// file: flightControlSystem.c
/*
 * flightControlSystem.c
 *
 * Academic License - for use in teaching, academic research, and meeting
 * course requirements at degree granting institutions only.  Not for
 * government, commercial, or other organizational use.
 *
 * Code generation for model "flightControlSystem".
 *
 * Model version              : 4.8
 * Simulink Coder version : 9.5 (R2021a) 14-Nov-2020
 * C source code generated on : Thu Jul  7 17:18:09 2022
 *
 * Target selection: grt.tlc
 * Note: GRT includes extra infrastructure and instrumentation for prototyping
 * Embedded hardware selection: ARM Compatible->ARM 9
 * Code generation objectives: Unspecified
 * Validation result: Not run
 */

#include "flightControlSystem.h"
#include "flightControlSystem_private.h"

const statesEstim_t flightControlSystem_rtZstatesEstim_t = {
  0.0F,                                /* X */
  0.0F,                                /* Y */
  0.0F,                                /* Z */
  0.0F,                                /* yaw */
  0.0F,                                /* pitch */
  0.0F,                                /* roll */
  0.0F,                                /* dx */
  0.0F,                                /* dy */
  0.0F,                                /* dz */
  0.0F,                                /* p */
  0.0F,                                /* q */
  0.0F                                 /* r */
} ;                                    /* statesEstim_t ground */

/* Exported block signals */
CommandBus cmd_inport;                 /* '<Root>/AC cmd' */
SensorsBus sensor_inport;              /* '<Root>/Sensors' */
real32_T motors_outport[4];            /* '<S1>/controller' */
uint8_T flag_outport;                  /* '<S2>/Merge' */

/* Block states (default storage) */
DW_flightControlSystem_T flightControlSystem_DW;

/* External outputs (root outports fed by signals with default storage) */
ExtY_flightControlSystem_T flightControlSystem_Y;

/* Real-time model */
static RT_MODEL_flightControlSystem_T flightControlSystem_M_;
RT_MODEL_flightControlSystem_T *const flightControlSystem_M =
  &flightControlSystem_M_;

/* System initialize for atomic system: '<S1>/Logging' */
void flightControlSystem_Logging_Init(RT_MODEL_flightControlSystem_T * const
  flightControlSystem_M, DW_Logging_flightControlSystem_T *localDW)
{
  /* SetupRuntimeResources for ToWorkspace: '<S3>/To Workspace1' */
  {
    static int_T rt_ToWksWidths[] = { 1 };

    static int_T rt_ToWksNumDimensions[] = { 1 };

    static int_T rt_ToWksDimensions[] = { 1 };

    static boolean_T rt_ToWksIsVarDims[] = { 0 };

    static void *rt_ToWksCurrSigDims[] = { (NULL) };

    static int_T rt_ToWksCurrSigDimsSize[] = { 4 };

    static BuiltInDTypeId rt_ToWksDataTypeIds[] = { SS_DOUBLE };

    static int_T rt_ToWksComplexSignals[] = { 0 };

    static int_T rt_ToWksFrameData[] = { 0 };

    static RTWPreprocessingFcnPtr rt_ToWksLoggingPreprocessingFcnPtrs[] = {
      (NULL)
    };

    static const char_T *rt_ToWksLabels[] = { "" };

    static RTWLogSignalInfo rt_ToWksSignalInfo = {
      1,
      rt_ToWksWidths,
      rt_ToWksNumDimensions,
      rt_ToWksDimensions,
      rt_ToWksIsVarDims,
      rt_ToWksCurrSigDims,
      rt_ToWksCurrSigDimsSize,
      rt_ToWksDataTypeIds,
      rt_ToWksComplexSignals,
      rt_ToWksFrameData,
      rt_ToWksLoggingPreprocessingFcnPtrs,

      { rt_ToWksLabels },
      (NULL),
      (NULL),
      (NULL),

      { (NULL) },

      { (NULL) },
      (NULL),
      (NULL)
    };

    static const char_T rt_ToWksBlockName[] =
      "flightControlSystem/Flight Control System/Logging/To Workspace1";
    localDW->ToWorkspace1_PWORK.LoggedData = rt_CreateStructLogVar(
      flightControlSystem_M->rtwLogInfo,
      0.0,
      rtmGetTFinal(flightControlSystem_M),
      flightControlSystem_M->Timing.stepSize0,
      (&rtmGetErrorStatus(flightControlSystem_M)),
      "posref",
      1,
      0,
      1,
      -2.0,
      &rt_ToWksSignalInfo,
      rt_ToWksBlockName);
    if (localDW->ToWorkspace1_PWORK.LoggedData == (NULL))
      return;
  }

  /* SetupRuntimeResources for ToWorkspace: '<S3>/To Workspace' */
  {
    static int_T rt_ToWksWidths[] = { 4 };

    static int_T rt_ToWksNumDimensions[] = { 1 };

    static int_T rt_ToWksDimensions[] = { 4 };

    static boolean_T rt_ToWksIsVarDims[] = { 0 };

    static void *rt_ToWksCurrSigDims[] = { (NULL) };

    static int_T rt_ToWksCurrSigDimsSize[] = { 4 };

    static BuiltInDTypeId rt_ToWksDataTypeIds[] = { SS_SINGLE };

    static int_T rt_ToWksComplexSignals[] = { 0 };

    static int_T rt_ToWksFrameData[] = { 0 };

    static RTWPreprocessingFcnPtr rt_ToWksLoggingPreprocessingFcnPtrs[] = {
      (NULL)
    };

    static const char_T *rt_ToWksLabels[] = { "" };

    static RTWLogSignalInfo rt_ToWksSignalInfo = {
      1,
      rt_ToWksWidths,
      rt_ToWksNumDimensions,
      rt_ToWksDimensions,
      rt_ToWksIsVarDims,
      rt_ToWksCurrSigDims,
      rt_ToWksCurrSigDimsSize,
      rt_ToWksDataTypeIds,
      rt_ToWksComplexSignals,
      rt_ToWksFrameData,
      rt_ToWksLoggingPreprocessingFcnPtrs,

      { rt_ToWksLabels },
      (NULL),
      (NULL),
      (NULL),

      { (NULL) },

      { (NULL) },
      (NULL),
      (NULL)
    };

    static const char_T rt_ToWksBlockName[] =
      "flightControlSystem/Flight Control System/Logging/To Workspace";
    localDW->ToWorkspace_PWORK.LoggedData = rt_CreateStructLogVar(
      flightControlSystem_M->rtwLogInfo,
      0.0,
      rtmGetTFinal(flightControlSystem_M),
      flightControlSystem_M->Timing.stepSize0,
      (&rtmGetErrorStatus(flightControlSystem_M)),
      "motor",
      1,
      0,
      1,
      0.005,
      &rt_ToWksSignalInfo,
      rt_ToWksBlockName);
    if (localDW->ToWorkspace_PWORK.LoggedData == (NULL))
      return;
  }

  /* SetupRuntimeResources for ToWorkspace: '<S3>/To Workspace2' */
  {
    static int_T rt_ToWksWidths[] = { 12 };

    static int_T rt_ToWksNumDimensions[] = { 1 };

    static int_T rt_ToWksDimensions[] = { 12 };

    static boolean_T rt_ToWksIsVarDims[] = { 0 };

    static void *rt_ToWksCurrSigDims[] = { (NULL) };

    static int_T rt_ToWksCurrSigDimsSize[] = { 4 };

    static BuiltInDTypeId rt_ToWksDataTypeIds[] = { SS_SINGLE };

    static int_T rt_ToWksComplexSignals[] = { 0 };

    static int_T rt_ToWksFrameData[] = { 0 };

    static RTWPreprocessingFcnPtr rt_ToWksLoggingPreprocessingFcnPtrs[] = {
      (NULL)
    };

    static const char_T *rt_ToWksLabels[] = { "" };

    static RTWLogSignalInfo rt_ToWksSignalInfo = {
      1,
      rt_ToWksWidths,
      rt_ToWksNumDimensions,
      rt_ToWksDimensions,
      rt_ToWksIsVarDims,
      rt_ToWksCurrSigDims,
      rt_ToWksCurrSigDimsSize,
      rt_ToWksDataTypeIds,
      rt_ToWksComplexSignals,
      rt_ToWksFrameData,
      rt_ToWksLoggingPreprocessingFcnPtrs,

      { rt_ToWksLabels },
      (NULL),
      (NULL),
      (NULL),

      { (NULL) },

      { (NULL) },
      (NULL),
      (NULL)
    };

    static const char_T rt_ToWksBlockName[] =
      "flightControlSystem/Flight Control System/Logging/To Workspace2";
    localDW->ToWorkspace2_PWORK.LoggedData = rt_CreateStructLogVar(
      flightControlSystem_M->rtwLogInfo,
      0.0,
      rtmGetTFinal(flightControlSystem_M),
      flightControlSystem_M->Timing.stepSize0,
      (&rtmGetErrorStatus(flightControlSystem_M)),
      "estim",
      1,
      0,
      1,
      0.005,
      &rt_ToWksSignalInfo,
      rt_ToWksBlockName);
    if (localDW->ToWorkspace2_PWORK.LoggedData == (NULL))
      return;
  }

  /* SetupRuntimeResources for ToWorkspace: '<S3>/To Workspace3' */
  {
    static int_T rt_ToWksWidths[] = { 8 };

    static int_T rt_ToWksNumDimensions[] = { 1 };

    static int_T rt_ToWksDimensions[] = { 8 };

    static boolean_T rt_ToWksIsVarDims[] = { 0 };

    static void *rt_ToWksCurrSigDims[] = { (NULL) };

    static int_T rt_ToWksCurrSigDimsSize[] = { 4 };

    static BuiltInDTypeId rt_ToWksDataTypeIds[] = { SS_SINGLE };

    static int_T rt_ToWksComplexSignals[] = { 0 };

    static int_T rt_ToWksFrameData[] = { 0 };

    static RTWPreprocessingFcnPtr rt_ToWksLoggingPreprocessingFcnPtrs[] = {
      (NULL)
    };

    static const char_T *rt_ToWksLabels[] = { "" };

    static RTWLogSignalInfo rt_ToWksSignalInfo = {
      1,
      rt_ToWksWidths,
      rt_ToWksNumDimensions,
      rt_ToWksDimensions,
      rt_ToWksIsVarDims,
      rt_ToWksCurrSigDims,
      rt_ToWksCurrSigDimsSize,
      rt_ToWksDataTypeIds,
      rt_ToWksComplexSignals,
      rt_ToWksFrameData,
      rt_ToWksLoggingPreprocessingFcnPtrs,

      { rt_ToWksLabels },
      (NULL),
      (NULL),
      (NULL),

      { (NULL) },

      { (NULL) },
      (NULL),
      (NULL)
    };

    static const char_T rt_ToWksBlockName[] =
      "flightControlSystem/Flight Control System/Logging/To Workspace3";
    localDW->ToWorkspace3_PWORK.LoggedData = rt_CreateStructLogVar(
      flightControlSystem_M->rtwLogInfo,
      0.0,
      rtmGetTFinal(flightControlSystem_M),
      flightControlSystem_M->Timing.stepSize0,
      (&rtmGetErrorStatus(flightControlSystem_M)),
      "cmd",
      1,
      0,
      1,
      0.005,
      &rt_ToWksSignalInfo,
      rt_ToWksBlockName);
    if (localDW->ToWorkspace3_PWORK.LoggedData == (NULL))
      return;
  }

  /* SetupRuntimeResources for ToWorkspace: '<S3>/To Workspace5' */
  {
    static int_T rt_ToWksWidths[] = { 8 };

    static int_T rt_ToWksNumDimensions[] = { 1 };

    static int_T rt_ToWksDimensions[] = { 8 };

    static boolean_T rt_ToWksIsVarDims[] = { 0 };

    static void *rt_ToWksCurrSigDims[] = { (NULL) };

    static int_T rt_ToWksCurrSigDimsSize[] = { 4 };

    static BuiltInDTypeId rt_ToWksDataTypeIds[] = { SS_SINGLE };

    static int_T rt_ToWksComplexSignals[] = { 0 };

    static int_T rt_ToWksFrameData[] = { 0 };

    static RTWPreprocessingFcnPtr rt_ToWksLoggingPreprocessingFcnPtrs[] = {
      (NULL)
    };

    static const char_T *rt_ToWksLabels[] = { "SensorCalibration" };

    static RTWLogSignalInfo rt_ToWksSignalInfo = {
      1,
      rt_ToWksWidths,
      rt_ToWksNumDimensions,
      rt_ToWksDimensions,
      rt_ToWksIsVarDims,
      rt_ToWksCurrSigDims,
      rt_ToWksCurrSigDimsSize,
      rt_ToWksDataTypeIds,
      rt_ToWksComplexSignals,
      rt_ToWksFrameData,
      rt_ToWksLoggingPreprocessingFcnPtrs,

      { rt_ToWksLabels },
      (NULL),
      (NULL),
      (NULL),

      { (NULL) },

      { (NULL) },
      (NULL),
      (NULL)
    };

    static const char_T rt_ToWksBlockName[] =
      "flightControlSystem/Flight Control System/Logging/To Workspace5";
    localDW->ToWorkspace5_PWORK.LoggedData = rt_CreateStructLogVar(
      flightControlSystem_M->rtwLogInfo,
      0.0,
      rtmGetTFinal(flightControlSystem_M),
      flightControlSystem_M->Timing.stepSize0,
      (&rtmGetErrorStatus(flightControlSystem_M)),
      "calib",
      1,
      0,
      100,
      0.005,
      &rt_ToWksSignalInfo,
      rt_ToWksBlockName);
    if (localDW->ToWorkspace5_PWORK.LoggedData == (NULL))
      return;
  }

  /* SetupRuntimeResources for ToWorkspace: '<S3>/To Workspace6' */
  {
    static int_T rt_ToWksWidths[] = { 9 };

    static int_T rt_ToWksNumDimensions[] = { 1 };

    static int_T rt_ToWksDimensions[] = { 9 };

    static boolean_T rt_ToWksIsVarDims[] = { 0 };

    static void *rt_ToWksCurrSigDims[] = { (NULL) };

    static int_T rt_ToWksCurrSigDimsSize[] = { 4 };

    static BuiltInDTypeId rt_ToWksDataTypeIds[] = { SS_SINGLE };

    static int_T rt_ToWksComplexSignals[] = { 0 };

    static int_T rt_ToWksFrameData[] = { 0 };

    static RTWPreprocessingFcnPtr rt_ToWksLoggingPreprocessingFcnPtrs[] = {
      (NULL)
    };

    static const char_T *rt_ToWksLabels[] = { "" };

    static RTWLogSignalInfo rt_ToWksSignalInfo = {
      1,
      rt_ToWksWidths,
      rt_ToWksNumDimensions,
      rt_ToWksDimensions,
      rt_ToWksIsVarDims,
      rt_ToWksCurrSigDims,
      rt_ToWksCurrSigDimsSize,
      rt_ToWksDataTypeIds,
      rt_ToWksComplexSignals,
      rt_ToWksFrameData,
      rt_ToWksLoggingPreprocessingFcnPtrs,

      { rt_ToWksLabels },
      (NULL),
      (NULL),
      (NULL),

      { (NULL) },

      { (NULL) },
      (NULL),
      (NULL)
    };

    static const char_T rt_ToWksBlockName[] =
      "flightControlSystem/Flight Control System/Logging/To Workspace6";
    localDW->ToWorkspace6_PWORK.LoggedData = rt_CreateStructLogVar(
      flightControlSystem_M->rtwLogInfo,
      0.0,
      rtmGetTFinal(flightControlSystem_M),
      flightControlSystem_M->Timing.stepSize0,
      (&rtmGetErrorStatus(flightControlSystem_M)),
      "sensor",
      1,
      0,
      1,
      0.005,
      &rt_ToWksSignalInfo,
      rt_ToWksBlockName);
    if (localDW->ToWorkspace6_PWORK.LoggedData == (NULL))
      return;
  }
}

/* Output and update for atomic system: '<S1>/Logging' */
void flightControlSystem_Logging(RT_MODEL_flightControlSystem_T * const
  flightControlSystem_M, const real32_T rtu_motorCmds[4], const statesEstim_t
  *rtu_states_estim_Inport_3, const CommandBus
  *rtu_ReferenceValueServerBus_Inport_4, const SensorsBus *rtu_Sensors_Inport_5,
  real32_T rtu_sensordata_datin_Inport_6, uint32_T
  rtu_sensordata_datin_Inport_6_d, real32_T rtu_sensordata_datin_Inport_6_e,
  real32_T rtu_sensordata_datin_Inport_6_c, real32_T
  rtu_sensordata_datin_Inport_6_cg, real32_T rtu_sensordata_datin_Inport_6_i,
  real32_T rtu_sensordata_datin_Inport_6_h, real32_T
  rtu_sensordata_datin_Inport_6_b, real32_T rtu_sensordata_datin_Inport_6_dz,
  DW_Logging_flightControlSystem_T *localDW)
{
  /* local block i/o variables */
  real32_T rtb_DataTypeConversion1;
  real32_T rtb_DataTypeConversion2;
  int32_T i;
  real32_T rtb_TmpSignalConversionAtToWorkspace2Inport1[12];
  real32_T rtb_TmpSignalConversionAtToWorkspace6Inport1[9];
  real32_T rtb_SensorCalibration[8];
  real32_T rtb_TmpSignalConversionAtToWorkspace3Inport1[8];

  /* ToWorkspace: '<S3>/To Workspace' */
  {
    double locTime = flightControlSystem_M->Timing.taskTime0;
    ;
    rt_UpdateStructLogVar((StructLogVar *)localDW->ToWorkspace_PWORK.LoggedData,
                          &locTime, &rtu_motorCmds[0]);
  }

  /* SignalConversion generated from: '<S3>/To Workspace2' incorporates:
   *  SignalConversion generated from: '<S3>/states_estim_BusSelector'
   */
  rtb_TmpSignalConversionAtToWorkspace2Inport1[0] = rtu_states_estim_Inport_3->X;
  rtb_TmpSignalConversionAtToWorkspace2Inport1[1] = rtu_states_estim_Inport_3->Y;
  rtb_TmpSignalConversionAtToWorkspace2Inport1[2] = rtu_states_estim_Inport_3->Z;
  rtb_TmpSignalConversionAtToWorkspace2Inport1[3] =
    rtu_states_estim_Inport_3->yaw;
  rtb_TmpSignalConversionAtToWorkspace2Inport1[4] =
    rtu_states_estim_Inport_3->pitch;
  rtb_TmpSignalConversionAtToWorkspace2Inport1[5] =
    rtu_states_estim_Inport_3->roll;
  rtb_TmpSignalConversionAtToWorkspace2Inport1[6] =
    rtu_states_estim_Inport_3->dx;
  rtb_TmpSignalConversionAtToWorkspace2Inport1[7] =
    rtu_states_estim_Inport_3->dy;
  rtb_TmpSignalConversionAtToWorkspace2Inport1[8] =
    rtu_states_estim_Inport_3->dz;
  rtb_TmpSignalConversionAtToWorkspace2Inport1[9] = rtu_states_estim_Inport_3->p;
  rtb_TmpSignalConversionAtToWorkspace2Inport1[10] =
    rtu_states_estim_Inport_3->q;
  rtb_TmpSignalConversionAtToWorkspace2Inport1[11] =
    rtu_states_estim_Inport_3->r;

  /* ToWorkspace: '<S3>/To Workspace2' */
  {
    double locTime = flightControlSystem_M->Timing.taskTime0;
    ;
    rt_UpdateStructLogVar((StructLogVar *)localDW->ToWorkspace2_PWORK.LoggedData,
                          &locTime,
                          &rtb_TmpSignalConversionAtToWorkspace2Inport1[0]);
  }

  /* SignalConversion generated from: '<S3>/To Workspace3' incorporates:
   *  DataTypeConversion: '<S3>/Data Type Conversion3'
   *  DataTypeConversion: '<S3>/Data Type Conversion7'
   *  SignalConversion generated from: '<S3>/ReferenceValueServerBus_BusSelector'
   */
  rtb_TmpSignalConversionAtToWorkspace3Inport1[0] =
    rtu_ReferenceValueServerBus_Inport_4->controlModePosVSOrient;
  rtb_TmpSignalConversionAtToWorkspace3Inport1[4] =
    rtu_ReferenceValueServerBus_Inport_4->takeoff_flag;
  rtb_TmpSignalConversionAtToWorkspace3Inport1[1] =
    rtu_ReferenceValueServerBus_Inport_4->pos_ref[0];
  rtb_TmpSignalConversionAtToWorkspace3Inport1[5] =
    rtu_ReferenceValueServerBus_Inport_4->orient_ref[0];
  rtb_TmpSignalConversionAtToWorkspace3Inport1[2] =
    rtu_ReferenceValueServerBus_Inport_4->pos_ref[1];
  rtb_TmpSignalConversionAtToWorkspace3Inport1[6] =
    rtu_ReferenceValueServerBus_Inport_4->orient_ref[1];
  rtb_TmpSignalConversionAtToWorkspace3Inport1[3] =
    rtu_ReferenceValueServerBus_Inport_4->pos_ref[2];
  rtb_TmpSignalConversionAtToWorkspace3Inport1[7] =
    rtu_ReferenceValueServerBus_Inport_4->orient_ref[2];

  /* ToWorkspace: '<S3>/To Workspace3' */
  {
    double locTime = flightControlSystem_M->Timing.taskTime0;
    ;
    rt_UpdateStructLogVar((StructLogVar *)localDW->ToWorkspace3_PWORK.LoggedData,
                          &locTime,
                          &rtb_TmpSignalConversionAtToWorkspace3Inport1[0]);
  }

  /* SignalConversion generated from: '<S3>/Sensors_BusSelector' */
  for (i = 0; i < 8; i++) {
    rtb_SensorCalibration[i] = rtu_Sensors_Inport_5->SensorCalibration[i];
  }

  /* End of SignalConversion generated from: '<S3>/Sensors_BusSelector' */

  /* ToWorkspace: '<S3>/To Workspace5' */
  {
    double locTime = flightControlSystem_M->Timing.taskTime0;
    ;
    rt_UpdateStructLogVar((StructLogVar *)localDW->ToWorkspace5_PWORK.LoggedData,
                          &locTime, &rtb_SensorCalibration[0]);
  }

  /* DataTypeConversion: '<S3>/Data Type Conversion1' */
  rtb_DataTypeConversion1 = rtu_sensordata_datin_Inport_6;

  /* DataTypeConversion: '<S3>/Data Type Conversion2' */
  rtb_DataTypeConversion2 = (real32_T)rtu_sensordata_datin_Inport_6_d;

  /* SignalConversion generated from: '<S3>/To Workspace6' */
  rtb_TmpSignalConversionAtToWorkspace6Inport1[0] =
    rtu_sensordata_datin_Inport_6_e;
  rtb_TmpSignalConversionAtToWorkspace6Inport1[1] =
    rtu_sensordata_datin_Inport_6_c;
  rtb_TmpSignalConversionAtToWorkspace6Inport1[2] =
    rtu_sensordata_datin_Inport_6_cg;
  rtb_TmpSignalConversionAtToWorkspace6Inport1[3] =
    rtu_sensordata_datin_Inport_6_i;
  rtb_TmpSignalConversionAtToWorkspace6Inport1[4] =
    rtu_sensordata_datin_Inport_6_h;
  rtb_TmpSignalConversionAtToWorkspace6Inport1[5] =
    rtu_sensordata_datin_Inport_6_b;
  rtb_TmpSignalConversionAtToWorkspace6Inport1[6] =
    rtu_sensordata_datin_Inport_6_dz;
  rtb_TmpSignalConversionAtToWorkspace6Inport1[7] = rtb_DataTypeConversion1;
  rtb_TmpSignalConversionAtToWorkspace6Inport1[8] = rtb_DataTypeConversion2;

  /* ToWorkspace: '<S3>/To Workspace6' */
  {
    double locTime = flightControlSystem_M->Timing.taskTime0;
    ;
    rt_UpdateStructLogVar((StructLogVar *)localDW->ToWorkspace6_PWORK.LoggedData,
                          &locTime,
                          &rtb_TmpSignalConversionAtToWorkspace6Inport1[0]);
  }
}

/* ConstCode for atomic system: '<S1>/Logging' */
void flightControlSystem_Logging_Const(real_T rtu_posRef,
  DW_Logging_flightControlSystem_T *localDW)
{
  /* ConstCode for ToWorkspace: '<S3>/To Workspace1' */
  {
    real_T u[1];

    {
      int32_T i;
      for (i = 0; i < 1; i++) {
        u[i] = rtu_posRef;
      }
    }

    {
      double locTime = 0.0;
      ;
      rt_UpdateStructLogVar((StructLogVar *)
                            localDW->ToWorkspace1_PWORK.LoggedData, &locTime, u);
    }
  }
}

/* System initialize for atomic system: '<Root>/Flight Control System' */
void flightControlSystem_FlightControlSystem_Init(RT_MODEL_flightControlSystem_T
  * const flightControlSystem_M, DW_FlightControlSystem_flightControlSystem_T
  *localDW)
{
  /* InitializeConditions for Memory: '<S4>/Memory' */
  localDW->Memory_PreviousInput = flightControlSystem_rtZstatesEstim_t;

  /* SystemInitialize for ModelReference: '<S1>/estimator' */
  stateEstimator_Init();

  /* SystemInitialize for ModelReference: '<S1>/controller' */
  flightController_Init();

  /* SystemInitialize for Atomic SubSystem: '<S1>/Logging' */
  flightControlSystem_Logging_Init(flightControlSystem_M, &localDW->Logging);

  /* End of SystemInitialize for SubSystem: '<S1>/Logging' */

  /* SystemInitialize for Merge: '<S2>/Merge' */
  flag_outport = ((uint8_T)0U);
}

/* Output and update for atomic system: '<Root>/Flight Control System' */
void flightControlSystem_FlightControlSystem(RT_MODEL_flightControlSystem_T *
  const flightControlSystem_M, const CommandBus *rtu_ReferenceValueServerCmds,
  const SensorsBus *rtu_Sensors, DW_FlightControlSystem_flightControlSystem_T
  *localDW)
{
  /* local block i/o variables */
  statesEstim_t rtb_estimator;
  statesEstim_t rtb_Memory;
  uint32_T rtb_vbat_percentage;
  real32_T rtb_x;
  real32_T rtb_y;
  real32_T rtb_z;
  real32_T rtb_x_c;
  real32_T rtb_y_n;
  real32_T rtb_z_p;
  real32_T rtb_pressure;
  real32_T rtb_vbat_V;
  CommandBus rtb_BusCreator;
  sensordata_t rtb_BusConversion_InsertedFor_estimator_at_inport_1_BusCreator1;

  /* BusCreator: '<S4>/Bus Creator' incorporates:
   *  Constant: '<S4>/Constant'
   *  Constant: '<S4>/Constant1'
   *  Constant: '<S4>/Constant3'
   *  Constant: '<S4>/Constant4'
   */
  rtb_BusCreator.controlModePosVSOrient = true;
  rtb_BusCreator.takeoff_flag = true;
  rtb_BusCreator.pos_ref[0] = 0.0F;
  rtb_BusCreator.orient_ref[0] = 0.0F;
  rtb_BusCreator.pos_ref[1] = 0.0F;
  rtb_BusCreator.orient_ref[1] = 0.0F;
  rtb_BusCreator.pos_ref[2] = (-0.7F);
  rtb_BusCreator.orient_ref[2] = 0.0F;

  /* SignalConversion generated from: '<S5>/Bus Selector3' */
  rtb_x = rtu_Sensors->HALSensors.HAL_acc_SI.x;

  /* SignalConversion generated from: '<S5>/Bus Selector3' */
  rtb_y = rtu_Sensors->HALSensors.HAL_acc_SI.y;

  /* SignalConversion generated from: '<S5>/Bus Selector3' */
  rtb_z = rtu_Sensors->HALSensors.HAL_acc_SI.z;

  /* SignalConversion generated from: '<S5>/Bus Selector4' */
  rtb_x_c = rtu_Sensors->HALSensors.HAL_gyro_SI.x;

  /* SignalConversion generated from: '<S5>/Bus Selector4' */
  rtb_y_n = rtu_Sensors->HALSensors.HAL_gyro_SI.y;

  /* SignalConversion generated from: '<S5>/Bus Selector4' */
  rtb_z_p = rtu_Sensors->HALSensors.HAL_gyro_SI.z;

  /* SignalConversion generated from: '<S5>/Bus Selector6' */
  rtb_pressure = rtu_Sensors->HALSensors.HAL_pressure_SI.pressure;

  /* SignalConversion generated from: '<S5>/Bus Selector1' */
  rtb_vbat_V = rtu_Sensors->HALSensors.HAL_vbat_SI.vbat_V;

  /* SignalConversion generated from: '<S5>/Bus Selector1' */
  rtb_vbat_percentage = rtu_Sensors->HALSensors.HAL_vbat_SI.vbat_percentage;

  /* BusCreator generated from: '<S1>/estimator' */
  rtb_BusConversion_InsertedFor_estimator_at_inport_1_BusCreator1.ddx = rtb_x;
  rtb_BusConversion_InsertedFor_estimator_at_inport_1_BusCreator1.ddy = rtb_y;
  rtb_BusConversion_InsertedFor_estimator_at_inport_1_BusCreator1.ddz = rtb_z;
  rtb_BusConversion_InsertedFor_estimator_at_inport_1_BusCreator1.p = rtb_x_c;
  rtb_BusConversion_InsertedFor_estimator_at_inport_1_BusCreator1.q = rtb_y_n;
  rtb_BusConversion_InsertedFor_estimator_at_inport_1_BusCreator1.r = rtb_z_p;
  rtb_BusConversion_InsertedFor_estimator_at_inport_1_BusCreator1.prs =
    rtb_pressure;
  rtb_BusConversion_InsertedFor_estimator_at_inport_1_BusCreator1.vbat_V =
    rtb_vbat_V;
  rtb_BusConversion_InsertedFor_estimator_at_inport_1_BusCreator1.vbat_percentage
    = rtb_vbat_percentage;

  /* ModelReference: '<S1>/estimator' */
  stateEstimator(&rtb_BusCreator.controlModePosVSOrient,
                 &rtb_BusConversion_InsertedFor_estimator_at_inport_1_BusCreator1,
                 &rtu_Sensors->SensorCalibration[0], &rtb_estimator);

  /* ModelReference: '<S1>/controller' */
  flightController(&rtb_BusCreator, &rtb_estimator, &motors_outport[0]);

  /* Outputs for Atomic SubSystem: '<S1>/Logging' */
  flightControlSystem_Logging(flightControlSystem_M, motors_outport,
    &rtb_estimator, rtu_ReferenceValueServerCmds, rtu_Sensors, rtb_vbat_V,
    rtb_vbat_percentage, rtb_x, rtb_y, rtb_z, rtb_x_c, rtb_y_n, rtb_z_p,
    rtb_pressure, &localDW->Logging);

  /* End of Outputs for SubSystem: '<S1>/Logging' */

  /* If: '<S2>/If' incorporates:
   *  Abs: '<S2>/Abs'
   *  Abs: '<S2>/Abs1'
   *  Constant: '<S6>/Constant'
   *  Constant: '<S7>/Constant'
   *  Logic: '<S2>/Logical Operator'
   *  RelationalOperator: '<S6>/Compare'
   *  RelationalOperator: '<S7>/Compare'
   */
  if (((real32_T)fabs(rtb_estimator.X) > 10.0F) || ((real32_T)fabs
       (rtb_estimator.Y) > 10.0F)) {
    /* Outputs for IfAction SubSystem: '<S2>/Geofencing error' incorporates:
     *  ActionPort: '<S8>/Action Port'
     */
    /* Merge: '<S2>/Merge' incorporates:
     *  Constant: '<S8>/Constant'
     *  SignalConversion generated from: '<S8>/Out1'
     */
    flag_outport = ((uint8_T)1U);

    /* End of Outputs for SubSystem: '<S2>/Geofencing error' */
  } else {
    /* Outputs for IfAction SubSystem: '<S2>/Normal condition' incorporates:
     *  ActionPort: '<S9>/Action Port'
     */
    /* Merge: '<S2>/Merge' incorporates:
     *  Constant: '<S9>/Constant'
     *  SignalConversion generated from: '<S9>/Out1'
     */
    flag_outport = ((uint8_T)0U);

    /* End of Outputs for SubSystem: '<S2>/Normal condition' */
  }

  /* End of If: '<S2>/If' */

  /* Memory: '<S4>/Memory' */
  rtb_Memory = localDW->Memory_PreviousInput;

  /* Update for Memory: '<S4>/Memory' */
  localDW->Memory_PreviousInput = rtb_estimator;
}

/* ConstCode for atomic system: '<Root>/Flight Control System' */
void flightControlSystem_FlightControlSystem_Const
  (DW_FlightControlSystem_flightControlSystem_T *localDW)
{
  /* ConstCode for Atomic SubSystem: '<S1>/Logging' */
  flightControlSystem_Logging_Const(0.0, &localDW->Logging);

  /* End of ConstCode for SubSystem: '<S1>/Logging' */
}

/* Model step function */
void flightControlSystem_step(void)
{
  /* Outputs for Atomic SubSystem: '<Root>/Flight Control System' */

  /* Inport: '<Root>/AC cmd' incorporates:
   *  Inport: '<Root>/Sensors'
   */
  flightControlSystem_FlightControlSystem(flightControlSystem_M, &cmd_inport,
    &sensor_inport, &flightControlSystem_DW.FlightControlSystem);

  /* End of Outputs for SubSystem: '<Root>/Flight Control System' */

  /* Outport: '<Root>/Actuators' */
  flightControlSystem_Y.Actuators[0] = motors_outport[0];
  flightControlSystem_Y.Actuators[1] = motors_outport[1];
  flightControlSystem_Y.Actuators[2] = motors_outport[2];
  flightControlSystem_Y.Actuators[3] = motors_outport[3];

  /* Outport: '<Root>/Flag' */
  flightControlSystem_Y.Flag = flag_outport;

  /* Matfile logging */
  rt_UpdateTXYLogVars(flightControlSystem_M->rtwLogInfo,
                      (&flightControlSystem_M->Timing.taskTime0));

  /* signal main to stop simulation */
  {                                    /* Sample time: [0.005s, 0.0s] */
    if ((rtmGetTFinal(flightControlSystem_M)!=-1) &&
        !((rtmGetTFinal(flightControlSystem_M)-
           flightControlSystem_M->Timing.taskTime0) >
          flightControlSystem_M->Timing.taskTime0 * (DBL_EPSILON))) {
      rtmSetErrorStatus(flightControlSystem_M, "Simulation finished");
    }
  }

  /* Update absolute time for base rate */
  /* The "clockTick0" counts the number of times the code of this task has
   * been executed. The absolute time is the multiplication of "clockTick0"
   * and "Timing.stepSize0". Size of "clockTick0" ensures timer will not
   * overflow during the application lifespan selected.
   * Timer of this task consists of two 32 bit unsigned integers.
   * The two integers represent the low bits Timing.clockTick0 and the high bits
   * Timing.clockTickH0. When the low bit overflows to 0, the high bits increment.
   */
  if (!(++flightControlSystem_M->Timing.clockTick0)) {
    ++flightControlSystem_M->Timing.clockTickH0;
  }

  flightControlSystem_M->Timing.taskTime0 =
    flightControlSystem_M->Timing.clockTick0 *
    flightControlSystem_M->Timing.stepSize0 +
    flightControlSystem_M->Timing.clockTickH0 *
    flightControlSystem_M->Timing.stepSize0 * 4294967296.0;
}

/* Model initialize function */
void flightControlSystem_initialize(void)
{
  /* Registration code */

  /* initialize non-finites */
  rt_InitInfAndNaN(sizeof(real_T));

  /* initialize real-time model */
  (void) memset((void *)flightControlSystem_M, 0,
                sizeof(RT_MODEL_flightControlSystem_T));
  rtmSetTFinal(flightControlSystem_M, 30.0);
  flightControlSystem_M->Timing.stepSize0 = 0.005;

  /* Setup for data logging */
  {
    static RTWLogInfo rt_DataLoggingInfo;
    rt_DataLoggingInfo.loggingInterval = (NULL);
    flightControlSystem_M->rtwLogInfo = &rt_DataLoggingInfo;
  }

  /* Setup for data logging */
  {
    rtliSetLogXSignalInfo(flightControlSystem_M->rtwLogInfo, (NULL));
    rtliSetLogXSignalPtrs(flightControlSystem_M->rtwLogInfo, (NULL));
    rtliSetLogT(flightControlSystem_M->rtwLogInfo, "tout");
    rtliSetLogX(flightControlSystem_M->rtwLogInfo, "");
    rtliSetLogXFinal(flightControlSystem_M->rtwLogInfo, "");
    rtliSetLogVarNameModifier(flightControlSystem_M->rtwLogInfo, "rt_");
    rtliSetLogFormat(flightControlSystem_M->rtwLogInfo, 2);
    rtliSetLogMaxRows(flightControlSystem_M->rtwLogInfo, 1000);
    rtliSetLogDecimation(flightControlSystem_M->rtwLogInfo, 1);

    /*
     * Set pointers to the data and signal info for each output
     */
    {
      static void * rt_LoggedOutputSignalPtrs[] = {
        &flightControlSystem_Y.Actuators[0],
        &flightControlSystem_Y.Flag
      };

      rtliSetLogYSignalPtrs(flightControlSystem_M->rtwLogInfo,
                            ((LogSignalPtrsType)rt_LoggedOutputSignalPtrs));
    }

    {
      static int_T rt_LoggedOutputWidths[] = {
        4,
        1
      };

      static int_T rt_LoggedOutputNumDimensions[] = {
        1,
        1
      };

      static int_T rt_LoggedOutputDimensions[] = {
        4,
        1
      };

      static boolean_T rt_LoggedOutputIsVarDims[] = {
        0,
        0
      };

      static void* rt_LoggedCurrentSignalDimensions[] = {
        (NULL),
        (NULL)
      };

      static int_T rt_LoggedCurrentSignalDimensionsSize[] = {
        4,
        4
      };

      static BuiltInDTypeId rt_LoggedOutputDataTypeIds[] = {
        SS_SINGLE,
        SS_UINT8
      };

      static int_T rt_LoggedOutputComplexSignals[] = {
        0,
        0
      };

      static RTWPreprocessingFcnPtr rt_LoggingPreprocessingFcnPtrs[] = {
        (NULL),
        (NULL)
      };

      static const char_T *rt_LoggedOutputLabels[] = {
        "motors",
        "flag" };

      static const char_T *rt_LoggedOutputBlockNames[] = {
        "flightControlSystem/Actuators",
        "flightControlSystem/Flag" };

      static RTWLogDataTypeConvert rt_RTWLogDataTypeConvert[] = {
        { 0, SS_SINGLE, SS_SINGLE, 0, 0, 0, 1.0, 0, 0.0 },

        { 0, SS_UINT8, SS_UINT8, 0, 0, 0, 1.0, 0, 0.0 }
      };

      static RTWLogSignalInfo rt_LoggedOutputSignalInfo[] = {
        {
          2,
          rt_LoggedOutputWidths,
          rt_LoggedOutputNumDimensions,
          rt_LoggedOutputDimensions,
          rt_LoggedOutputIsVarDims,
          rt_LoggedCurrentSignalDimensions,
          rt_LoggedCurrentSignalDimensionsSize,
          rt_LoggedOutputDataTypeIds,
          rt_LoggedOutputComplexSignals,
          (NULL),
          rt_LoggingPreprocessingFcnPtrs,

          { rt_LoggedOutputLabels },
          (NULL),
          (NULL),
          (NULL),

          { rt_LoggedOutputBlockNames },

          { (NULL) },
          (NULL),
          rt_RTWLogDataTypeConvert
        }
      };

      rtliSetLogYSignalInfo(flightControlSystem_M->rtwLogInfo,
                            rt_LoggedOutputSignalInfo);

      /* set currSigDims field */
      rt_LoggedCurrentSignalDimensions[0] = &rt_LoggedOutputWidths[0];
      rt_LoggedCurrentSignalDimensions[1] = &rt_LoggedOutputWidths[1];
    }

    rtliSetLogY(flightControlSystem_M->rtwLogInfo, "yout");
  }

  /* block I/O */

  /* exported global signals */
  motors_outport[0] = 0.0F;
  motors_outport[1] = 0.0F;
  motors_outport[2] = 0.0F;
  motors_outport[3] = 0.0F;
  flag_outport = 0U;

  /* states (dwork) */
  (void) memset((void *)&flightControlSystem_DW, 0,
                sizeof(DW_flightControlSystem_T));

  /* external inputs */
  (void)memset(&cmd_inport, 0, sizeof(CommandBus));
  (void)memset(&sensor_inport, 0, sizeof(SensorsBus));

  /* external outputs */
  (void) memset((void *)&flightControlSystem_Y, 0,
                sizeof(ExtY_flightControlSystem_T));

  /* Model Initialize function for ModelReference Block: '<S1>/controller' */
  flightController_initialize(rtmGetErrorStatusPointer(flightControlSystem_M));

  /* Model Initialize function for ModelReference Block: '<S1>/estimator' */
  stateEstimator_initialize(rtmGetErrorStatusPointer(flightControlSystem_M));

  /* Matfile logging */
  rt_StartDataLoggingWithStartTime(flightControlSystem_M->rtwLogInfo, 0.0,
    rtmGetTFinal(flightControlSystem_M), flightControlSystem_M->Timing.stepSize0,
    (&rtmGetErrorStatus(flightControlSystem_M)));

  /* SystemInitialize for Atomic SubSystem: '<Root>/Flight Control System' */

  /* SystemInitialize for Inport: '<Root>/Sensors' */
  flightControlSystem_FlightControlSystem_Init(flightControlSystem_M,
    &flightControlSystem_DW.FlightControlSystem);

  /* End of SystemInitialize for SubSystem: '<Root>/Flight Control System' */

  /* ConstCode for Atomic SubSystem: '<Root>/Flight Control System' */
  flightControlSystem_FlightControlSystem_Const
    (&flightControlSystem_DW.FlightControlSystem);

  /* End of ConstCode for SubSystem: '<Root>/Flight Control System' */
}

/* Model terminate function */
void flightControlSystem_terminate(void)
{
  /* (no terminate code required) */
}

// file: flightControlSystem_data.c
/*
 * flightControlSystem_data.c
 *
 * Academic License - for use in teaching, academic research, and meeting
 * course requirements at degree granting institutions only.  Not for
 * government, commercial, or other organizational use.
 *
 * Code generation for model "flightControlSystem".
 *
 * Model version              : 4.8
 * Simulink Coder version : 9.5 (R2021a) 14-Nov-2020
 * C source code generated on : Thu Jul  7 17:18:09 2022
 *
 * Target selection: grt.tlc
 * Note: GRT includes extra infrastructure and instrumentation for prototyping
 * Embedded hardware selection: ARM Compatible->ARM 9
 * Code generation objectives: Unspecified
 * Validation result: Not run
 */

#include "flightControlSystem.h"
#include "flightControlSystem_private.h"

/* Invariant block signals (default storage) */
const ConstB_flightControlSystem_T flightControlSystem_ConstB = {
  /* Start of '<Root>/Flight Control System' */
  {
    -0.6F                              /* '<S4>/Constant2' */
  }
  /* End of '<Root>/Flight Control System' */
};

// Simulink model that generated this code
simulink model "flightControlSystem"  (R2021a)
settings: Solver=ode3  StartTime=0  StopTime=TFinal  FixedStep=Ts  RelTol=1e-3  EnableMultiTasking=on
undefined symbols (not defined in the file): landingAltitude, Ts
libraries: simulink x2

== system flightControlSystem ==
  note: Copyright 2013-2019 The MathWorks, Inc.
  note: Flight Control System
  AC cmd : Inport  OutDataTypeStr=Bus: CommandBus  BusOutputAsStruct=on
  Sensors : Inport  Port=2  OutDataTypeStr=Bus: SensorsBus  BusOutputAsStruct=on
  Flight Control System : Subsystem  TreatAsAtomicUnit=on  SystemSampleTime=Ts
  Actuators : Outport  OutDataTypeStr=single  PortDimensions=4  VectorParamsAs1DForOutWhenUnconnected=off
  Flag : Outport  Port=2  OutDataTypeStr=uint8  PortDimensions=1  VectorParamsAs1DForOutWhenUnconnected=off
  wires:
  AC cmd/1 -> Flight Control System/1(ReferenceValueServerCmds)  "cmd"
  Flight Control System/1(motorCmds) -> Actuators/1  "motors"
  Sensors/1 -> Flight Control System/2(Sensors)  "sensors"
  Flight Control System/2(Flag) -> Flag/1  "flag"

== system flightControlSystem/Flight Control System ==
  note: Derived from the work by Sertac
      | Karaman and Fabian Riether
  ReferenceValueServerCmds : Inport  OutDataTypeStr=Bus: CommandBus
  Sensors : Inport  Port=2  OutDataTypeStr=Bus: SensorsBus  BusOutputAsStruct=on
  Bus Selector : BusSelector  OutputSignals=SensorCalibration
  Bus Selector1 : BusSelector  OutputSignals=controlModePosVSOrient
  Bus Selector2 : BusSelector  OutputSignals=HAL_acc_SI,HAL_gyro_SI,HAL_pressure_SI,HAL_vbat_SI
  Bus Selector3 : BusSelector  OutputSignals=HALSensors
  Crash Predictor Flags : Subsystem
  Logging : Subsystem  TreatAsAtomicUnit=on
  Reference commands : Subsystem
  ReferenceValueServerCmds1 : InportShadow  OutDataTypeStr=Bus: CommandBus
  Sensors1 : InportShadow  Port=2  OutDataTypeStr=Bus: SensorsBus  BusOutputAsStruct=on
  Sensors2 : InportShadow  Port=2  OutDataTypeStr=Bus: SensorsBus  BusOutputAsStruct=on
  controller : ModelReference  ModelNameDialog=flightController.slx  SimulationMode=Normal  ModelReferenceVersion=4.2
  estimator : ModelReference  ModelNameDialog=stateEstimator.slx  SimulationMode=Normal  ModelReferenceVersion=4.8
  sensordata_group : Subsystem
  motorCmds : Outport  VectorParamsAs1DForOutWhenUnconnected=off
  Flag : Outport  Port=2  VectorParamsAs1DForOutWhenUnconnected=off
  wires:
  ReferenceValueServerCmds/1 -> Reference commands/1(serverCmd)
  Bus Selector2/1 -> sensordata_group/1(HAL_acc_SI)  "<HAL_acc_SI>"
  Bus Selector2/2 -> sensordata_group/2(HAL_gyro_SI)  "<HAL_gyro_SI>"
  estimator/1 -> Reference commands/2(states_estimout), Crash Predictor Flags/1(states_estim), Logging/3(states_estim), controller/2
  Sensors2/1 -> Logging/5(Sensors)
  ReferenceValueServerCmds1/1 -> Logging/4(ReferenceValueServerBus)
  controller/1 -> motorCmds/1, Logging/1(motorCmds)
  sensordata_group/1(sensordata_datin) -> Logging/6(sensordata_datin), estimator/2
  Bus Selector2/4 -> sensordata_group/4(HAL_vbat_SI)  "<HAL_vbat_SI>"
  Crash Predictor Flags/1(Flag) -> Flag/1
  Sensors/1 -> Bus Selector3/1
  Bus Selector3/1 -> Bus Selector2/1  "<HALSensors>"
  Sensors1/1 -> Bus Selector/1
  Bus Selector/1 -> estimator/3  "<SensorCalibration>"
  Bus Selector1/1 -> estimator/1  "<controlModePosVSOrient>"
  Reference commands/1(ReferenceValueCmds) -> Bus Selector1/1, controller/1
  Bus Selector2/3 -> sensordata_group/3(HAL_pressure_SI)  "<HAL_pressure_SI>"

== system flightControlSystem/Flight Control System/Crash Predictor Flags ==
  Bus Element In : Inport  PortName=states_estim  Element=X
  Bus Element In1 : Inport  PortName=states_estim  Element=Y
  Abs : Abs
  Abs1 : Abs
  Compare To Constant : simulink/Logic and Bit Operations/Compare To Constant  relop=>  const=10.0  OutDataTypeStr=boolean
  Compare To Constant1 : simulink/Logic and Bit Operations/Compare To Constant  relop=>  const=10.0  OutDataTypeStr=boolean
  Data Type Conversion : DataTypeConversion  OutDataTypeStr=uint8  RndMeth=Nearest
  Geofencing error : Subsystem  TreatAsAtomicUnit=on
  If : If
  Logical Operator : Logic  Operator=OR  AllPortsSameDT=off
  Merge : Merge  InitialOutput=0
  Normal condition : Subsystem  TreatAsAtomicUnit=on
  Flag : Outport  VectorParamsAs1DForOutWhenUnconnected=off
  wires:
  Bus Element In/1 -> Abs/1
  Bus Element In1/1 -> Abs1/1
  Compare To Constant/1 -> Logical Operator/1
  Compare To Constant1/1 -> Logical Operator/2
  Abs/1 -> Compare To Constant/1
  Abs1/1 -> Compare To Constant1/1
  Logical Operator/1 -> Data Type Conversion/1
  Merge/1 -> Flag/1
  If/1 -> Geofencing error/Action
  If/2 -> Normal condition/Action
  Geofencing error/1(Out1) -> Merge/1
  Normal condition/1(Out1) -> Merge/2
  Data Type Conversion/1 -> If/1

== system flightControlSystem/Flight Control System/Logging ==
  motorCmds : Inport
  posRef : Inport  Port=2
  Bus Element In : Inport  Port=3  PortName=states_estim  Element=X
  Bus Element In1 : Inport  Port=3  PortName=states_estim  Element=Y
  Bus Element In2 : Inport  Port=3  PortName=states_estim  Element=Z
  Bus Element In3 : Inport  Port=3  PortName=states_estim  Element=yaw
  Bus Element In6 : Inport  Port=3  PortName=states_estim  Element=dx
  Bus Element In5 : Inport  Port=3  PortName=states_estim  Element=roll
  Bus Element In4 : Inport  Port=3  PortName=states_estim  Element=pitch
  Bus Element In7 : Inport  Port=3  PortName=states_estim  Element=dy
  Bus Element In8 : Inport  Port=3  PortName=states_estim  Element=dz
  Bus Element In9 : Inport  Port=3  PortName=states_estim  Element=p
  Bus Element In10 : Inport  Port=3  PortName=states_estim  Element=q
  Bus Element In11 : Inport  Port=3  PortName=states_estim  Element=r
  Bus Element In12 : Inport  Port=4  PortName=ReferenceValueServerBus  Element=controlModePosVSOrient
  Bus Element In13 : Inport  Port=4  PortName=ReferenceValueServerBus  Element=pos_ref
  Bus Element In14 : Inport  Port=4  PortName=ReferenceValueServerBus  Element=takeoff_flag
  Bus Element In15 : Inport  Port=4  PortName=ReferenceValueServerBus  Element=orient_ref
  Bus Element In20 : Inport  Port=5  PortName=Sensors  Element=SensorCalibration
  Bus Element In21 : Inport  Port=6  PortName=sensordata_datin  Element=ddx
  Bus Element In22 : Inport  Port=6  PortName=sensordata_datin  Element=ddy
  Bus Element In23 : Inport  Port=6  PortName=sensordata_datin  Element=ddz
  Bus Element In24 : Inport  Port=6  PortName=sensordata_datin  Element=p
  Bus Element In25 : Inport  Port=6  PortName=sensordata_datin  Element=q
  Bus Element In26 : Inport  Port=6  PortName=sensordata_datin  Element=r
  Bus Element In28 : Inport  Port=6  PortName=sensordata_datin  Element=prs
  Bus Element In29 : Inport  Port=6  PortName=sensordata_datin  Element=vbat_percentage
  Bus Element In30 : Inport  Port=6  PortName=sensordata_datin  Element=vbat_V
  Data Type Conversion{1..3,7} (4 alike) : DataTypeConversion  OutDataTypeStr=single
  Mux1 : Mux
  Mux2 : Mux  Inputs=12
  Mux3 : Mux  Inputs=9
  To Workspace : ToWorkspace  VariableName=motor  SaveFormat=Structure With Time  SampleTime=-1
  To Workspace1 : ToWorkspace  VariableName=posref  SaveFormat=Structure With Time  SampleTime=-1
  To Workspace2 : ToWorkspace  VariableName=estim  SaveFormat=Structure With Time  SampleTime=-1
  To Workspace3 : ToWorkspace  VariableName=cmd  SaveFormat=Structure With Time  SampleTime=-1
  To Workspace5 : ToWorkspace  VariableName=calib  SaveFormat=Structure With Time  SampleTime=-1
  To Workspace6 : ToWorkspace  VariableName=sensor  SaveFormat=Structure With Time  SampleTime=-1
  wires:
  Bus Element In12/1 -> Data Type Conversion3/1
  Bus Element In14/1 -> Data Type Conversion7/1
  Bus Element In20/1 -> To Workspace5/1
  Mux2/1 -> To Workspace2/1
  motorCmds/1 -> To Workspace/1
  Mux1/1 -> To Workspace3/1
  Bus Element In3/1 -> Mux2/4
  Bus Element In5/1 -> Mux2/6
  Bus Element In4/1 -> Mux2/5
  Bus Element In8/1 -> Mux2/9
  Bus Element In6/1 -> Mux2/7
  Bus Element In7/1 -> Mux2/8
  Bus Element In9/1 -> Mux2/10
  Bus Element In11/1 -> Mux2/12
  Bus Element In1/1 -> Mux2/2
  Bus Element In10/1 -> Mux2/11
  Bus Element In2/1 -> Mux2/3
  Bus Element In/1 -> Mux2/1
  Data Type Conversion3/1 -> Mux1/1
  Bus Element In13/1 -> Mux1/2
  Data Type Conversion7/1 -> Mux1/3
  Bus Element In15/1 -> Mux1/4
  posRef/1 -> To Workspace1/1
  Bus Element In21/1 -> Mux3/1
  Bus Element In22/1 -> Mux3/2
  Bus Element In23/1 -> Mux3/3
  Bus Element In24/1 -> Mux3/4
  Bus Element In25/1 -> Mux3/5
  Bus Element In26/1 -> Mux3/6
  Bus Element In30/1 -> Data Type Conversion1/1
  Bus Element In29/1 -> Data Type Conversion2/1
  Mux3/1 -> To Workspace6/1
  Data Type Conversion1/1 -> Mux3/8
  Data Type Conversion2/1 -> Mux3/9
  Bus Element In28/1 -> Mux3/7

== system flightControlSystem/Flight Control System/Reference commands ==
  serverCmd : Inport
  states_estimout : Inport  Port=2
  Bus Creator : BusCreator  Inputs=4  OutDataTypeStr=Bus: CommandBus  NonVirtualBus=on
  Bus Selector : BusSelector  OutputSignals=X,Y
  Bus Selector1 : BusSelector  OutputSignals=takeoff_flag
  Constant : Constant  Value=[0 0 -0.7]  OutDataTypeStr=single
  Constant1 : Constant  Value=true  OutDataTypeStr=boolean
  Constant2 : Constant  Value=landingAltitude  OutDataTypeStr=single
  Constant3 : Constant  Value=[0 0 0]  OutDataTypeStr=single
  Constant4 : Constant  Value=true  OutDataTypeStr=boolean
  Memory : Memory  InheritSampleTime=on
  Mux : Mux  Inputs=3
  Terminator : Terminator
  Terminator1 : Terminator
  ReferenceValueCmds : Outport  OutDataTypeStr=Bus: CommandBus  VectorParamsAs1DForOutWhenUnconnected=off
  wires:
  Mux/1 -> Terminator/1  "pos_ref"
  Constant1/1 -> Bus Creator/1  "controlModePosVSOrient"
  Bus Selector1/1 -> Terminator1/1  "<takeoff_flag>"
  states_estimout/1 -> Memory/1
  Bus Selector/1 -> Mux/1  "<X>"
  Constant2/1 -> Mux/3
  Bus Selector/2 -> Mux/2  "<Y>"
  serverCmd/1 -> Bus Selector1/1
  Constant3/1 -> Bus Creator/4  "orient_ref"
  Memory/1 -> Bus Selector/1
  Bus Creator/1 -> ReferenceValueCmds/1
  Constant/1 -> Bus Creator/2  "pos_ref"
  Constant4/1 -> Bus Creator/3  "takeoff_flag"

== system flightControlSystem/Flight Control System/sensordata_group ==
  HAL_acc_SI : Inport  OutDataTypeStr=Bus: HAL_acc_SI_t
  HAL_gyro_SI : Inport  Port=2  OutDataTypeStr=Bus: HAL_gyro_SI_t
  HAL_pressure_SI : Inport  Port=3  OutDataTypeStr=Bus: HAL_pressure_SI_t
  HAL_vbat_SI : Inport  Port=4  OutDataTypeStr=Bus: HAL_vbat_SI_t
  Bus Selector1 : BusSelector  OutputSignals=vbat_V,vbat_percentage
  Bus Selector3 : BusSelector  OutputSignals=x,y,z
  Bus Selector4 : BusSelector  OutputSignals=x,y,z
  Bus Selector6 : BusSelector  OutputSignals=pressure
  Out Bus Element : Outport  VectorParamsAs1DForOutWhenUnconnected=off  PortName=sensordata_datin  Element=ddx
  Out Bus Element1 : Outport  VectorParamsAs1DForOutWhenUnconnected=off  PortName=sensordata_datin  Element=ddy
  Out Bus Element2 : Outport  VectorParamsAs1DForOutWhenUnconnected=off  PortName=sensordata_datin  Element=ddz
  Out Bus Element3 : Outport  VectorParamsAs1DForOutWhenUnconnected=off  PortName=sensordata_datin  Element=p
  Out Bus Element4 : Outport  VectorParamsAs1DForOutWhenUnconnected=off  PortName=sensordata_datin  Element=q
  Out Bus Element5 : Outport  VectorParamsAs1DForOutWhenUnconnected=off  PortName=sensordata_datin  Element=r
  Out Bus Element7 : Outport  VectorParamsAs1DForOutWhenUnconnected=off  PortName=sensordata_datin  Element=prs
  Out Bus Element8 : Outport  VectorParamsAs1DForOutWhenUnconnected=off  PortName=sensordata_datin  Element=vbat_V
  Out Bus Element9 : Outport  VectorParamsAs1DForOutWhenUnconnected=off  PortName=sensordata_datin  Element=vbat_percentage
  wires:
  HAL_gyro_SI/1 -> Bus Selector4/1
  HAL_acc_SI/1 -> Bus Selector3/1
  HAL_pressure_SI/1 -> Bus Selector6/1
  Bus Selector4/1 -> Out Bus Element3/1  "<x>"
  Bus Selector3/3 -> Out Bus Element2/1  "<z>"
  Bus Selector4/3 -> Out Bus Element5/1  "<z>"
  Bus Selector6/1 -> Out Bus Element7/1  "<pressure>"
  Bus Selector4/2 -> Out Bus Element4/1  "<y>"
  Bus Selector3/1 -> Out Bus Element/1  "<x>"
  Bus Selector3/2 -> Out Bus Element1/1  "<y>"
  Bus Selector1/1 -> Out Bus Element8/1  "<vbat_V>"
  HAL_vbat_SI/1 -> Bus Selector1/1
  Bus Selector1/2 -> Out Bus Element9/1  "<vbat_percentage>"

== system flightControlSystem/Flight Control System/Crash Predictor Flags/Geofencing error ==
  Action Port : ActionPort  ActionPortLabel=if(u1 > 0)
  Constant : Constant  OutDataTypeStr=uint8
  Out1 : Outport  VectorParamsAs1DForOutWhenUnconnected=off
  wires:
  Constant/1 -> Out1/1

== system flightControlSystem/Flight Control System/Crash Predictor Flags/Normal condition ==
  Action Port : ActionPort  ActionPortLabel=else
  Constant : Constant  Value=0  OutDataTypeStr=uint8
  Out1 : Outport  VectorParamsAs1DForOutWhenUnconnected=off
  wires:
  Constant/1 -> Out1/1
